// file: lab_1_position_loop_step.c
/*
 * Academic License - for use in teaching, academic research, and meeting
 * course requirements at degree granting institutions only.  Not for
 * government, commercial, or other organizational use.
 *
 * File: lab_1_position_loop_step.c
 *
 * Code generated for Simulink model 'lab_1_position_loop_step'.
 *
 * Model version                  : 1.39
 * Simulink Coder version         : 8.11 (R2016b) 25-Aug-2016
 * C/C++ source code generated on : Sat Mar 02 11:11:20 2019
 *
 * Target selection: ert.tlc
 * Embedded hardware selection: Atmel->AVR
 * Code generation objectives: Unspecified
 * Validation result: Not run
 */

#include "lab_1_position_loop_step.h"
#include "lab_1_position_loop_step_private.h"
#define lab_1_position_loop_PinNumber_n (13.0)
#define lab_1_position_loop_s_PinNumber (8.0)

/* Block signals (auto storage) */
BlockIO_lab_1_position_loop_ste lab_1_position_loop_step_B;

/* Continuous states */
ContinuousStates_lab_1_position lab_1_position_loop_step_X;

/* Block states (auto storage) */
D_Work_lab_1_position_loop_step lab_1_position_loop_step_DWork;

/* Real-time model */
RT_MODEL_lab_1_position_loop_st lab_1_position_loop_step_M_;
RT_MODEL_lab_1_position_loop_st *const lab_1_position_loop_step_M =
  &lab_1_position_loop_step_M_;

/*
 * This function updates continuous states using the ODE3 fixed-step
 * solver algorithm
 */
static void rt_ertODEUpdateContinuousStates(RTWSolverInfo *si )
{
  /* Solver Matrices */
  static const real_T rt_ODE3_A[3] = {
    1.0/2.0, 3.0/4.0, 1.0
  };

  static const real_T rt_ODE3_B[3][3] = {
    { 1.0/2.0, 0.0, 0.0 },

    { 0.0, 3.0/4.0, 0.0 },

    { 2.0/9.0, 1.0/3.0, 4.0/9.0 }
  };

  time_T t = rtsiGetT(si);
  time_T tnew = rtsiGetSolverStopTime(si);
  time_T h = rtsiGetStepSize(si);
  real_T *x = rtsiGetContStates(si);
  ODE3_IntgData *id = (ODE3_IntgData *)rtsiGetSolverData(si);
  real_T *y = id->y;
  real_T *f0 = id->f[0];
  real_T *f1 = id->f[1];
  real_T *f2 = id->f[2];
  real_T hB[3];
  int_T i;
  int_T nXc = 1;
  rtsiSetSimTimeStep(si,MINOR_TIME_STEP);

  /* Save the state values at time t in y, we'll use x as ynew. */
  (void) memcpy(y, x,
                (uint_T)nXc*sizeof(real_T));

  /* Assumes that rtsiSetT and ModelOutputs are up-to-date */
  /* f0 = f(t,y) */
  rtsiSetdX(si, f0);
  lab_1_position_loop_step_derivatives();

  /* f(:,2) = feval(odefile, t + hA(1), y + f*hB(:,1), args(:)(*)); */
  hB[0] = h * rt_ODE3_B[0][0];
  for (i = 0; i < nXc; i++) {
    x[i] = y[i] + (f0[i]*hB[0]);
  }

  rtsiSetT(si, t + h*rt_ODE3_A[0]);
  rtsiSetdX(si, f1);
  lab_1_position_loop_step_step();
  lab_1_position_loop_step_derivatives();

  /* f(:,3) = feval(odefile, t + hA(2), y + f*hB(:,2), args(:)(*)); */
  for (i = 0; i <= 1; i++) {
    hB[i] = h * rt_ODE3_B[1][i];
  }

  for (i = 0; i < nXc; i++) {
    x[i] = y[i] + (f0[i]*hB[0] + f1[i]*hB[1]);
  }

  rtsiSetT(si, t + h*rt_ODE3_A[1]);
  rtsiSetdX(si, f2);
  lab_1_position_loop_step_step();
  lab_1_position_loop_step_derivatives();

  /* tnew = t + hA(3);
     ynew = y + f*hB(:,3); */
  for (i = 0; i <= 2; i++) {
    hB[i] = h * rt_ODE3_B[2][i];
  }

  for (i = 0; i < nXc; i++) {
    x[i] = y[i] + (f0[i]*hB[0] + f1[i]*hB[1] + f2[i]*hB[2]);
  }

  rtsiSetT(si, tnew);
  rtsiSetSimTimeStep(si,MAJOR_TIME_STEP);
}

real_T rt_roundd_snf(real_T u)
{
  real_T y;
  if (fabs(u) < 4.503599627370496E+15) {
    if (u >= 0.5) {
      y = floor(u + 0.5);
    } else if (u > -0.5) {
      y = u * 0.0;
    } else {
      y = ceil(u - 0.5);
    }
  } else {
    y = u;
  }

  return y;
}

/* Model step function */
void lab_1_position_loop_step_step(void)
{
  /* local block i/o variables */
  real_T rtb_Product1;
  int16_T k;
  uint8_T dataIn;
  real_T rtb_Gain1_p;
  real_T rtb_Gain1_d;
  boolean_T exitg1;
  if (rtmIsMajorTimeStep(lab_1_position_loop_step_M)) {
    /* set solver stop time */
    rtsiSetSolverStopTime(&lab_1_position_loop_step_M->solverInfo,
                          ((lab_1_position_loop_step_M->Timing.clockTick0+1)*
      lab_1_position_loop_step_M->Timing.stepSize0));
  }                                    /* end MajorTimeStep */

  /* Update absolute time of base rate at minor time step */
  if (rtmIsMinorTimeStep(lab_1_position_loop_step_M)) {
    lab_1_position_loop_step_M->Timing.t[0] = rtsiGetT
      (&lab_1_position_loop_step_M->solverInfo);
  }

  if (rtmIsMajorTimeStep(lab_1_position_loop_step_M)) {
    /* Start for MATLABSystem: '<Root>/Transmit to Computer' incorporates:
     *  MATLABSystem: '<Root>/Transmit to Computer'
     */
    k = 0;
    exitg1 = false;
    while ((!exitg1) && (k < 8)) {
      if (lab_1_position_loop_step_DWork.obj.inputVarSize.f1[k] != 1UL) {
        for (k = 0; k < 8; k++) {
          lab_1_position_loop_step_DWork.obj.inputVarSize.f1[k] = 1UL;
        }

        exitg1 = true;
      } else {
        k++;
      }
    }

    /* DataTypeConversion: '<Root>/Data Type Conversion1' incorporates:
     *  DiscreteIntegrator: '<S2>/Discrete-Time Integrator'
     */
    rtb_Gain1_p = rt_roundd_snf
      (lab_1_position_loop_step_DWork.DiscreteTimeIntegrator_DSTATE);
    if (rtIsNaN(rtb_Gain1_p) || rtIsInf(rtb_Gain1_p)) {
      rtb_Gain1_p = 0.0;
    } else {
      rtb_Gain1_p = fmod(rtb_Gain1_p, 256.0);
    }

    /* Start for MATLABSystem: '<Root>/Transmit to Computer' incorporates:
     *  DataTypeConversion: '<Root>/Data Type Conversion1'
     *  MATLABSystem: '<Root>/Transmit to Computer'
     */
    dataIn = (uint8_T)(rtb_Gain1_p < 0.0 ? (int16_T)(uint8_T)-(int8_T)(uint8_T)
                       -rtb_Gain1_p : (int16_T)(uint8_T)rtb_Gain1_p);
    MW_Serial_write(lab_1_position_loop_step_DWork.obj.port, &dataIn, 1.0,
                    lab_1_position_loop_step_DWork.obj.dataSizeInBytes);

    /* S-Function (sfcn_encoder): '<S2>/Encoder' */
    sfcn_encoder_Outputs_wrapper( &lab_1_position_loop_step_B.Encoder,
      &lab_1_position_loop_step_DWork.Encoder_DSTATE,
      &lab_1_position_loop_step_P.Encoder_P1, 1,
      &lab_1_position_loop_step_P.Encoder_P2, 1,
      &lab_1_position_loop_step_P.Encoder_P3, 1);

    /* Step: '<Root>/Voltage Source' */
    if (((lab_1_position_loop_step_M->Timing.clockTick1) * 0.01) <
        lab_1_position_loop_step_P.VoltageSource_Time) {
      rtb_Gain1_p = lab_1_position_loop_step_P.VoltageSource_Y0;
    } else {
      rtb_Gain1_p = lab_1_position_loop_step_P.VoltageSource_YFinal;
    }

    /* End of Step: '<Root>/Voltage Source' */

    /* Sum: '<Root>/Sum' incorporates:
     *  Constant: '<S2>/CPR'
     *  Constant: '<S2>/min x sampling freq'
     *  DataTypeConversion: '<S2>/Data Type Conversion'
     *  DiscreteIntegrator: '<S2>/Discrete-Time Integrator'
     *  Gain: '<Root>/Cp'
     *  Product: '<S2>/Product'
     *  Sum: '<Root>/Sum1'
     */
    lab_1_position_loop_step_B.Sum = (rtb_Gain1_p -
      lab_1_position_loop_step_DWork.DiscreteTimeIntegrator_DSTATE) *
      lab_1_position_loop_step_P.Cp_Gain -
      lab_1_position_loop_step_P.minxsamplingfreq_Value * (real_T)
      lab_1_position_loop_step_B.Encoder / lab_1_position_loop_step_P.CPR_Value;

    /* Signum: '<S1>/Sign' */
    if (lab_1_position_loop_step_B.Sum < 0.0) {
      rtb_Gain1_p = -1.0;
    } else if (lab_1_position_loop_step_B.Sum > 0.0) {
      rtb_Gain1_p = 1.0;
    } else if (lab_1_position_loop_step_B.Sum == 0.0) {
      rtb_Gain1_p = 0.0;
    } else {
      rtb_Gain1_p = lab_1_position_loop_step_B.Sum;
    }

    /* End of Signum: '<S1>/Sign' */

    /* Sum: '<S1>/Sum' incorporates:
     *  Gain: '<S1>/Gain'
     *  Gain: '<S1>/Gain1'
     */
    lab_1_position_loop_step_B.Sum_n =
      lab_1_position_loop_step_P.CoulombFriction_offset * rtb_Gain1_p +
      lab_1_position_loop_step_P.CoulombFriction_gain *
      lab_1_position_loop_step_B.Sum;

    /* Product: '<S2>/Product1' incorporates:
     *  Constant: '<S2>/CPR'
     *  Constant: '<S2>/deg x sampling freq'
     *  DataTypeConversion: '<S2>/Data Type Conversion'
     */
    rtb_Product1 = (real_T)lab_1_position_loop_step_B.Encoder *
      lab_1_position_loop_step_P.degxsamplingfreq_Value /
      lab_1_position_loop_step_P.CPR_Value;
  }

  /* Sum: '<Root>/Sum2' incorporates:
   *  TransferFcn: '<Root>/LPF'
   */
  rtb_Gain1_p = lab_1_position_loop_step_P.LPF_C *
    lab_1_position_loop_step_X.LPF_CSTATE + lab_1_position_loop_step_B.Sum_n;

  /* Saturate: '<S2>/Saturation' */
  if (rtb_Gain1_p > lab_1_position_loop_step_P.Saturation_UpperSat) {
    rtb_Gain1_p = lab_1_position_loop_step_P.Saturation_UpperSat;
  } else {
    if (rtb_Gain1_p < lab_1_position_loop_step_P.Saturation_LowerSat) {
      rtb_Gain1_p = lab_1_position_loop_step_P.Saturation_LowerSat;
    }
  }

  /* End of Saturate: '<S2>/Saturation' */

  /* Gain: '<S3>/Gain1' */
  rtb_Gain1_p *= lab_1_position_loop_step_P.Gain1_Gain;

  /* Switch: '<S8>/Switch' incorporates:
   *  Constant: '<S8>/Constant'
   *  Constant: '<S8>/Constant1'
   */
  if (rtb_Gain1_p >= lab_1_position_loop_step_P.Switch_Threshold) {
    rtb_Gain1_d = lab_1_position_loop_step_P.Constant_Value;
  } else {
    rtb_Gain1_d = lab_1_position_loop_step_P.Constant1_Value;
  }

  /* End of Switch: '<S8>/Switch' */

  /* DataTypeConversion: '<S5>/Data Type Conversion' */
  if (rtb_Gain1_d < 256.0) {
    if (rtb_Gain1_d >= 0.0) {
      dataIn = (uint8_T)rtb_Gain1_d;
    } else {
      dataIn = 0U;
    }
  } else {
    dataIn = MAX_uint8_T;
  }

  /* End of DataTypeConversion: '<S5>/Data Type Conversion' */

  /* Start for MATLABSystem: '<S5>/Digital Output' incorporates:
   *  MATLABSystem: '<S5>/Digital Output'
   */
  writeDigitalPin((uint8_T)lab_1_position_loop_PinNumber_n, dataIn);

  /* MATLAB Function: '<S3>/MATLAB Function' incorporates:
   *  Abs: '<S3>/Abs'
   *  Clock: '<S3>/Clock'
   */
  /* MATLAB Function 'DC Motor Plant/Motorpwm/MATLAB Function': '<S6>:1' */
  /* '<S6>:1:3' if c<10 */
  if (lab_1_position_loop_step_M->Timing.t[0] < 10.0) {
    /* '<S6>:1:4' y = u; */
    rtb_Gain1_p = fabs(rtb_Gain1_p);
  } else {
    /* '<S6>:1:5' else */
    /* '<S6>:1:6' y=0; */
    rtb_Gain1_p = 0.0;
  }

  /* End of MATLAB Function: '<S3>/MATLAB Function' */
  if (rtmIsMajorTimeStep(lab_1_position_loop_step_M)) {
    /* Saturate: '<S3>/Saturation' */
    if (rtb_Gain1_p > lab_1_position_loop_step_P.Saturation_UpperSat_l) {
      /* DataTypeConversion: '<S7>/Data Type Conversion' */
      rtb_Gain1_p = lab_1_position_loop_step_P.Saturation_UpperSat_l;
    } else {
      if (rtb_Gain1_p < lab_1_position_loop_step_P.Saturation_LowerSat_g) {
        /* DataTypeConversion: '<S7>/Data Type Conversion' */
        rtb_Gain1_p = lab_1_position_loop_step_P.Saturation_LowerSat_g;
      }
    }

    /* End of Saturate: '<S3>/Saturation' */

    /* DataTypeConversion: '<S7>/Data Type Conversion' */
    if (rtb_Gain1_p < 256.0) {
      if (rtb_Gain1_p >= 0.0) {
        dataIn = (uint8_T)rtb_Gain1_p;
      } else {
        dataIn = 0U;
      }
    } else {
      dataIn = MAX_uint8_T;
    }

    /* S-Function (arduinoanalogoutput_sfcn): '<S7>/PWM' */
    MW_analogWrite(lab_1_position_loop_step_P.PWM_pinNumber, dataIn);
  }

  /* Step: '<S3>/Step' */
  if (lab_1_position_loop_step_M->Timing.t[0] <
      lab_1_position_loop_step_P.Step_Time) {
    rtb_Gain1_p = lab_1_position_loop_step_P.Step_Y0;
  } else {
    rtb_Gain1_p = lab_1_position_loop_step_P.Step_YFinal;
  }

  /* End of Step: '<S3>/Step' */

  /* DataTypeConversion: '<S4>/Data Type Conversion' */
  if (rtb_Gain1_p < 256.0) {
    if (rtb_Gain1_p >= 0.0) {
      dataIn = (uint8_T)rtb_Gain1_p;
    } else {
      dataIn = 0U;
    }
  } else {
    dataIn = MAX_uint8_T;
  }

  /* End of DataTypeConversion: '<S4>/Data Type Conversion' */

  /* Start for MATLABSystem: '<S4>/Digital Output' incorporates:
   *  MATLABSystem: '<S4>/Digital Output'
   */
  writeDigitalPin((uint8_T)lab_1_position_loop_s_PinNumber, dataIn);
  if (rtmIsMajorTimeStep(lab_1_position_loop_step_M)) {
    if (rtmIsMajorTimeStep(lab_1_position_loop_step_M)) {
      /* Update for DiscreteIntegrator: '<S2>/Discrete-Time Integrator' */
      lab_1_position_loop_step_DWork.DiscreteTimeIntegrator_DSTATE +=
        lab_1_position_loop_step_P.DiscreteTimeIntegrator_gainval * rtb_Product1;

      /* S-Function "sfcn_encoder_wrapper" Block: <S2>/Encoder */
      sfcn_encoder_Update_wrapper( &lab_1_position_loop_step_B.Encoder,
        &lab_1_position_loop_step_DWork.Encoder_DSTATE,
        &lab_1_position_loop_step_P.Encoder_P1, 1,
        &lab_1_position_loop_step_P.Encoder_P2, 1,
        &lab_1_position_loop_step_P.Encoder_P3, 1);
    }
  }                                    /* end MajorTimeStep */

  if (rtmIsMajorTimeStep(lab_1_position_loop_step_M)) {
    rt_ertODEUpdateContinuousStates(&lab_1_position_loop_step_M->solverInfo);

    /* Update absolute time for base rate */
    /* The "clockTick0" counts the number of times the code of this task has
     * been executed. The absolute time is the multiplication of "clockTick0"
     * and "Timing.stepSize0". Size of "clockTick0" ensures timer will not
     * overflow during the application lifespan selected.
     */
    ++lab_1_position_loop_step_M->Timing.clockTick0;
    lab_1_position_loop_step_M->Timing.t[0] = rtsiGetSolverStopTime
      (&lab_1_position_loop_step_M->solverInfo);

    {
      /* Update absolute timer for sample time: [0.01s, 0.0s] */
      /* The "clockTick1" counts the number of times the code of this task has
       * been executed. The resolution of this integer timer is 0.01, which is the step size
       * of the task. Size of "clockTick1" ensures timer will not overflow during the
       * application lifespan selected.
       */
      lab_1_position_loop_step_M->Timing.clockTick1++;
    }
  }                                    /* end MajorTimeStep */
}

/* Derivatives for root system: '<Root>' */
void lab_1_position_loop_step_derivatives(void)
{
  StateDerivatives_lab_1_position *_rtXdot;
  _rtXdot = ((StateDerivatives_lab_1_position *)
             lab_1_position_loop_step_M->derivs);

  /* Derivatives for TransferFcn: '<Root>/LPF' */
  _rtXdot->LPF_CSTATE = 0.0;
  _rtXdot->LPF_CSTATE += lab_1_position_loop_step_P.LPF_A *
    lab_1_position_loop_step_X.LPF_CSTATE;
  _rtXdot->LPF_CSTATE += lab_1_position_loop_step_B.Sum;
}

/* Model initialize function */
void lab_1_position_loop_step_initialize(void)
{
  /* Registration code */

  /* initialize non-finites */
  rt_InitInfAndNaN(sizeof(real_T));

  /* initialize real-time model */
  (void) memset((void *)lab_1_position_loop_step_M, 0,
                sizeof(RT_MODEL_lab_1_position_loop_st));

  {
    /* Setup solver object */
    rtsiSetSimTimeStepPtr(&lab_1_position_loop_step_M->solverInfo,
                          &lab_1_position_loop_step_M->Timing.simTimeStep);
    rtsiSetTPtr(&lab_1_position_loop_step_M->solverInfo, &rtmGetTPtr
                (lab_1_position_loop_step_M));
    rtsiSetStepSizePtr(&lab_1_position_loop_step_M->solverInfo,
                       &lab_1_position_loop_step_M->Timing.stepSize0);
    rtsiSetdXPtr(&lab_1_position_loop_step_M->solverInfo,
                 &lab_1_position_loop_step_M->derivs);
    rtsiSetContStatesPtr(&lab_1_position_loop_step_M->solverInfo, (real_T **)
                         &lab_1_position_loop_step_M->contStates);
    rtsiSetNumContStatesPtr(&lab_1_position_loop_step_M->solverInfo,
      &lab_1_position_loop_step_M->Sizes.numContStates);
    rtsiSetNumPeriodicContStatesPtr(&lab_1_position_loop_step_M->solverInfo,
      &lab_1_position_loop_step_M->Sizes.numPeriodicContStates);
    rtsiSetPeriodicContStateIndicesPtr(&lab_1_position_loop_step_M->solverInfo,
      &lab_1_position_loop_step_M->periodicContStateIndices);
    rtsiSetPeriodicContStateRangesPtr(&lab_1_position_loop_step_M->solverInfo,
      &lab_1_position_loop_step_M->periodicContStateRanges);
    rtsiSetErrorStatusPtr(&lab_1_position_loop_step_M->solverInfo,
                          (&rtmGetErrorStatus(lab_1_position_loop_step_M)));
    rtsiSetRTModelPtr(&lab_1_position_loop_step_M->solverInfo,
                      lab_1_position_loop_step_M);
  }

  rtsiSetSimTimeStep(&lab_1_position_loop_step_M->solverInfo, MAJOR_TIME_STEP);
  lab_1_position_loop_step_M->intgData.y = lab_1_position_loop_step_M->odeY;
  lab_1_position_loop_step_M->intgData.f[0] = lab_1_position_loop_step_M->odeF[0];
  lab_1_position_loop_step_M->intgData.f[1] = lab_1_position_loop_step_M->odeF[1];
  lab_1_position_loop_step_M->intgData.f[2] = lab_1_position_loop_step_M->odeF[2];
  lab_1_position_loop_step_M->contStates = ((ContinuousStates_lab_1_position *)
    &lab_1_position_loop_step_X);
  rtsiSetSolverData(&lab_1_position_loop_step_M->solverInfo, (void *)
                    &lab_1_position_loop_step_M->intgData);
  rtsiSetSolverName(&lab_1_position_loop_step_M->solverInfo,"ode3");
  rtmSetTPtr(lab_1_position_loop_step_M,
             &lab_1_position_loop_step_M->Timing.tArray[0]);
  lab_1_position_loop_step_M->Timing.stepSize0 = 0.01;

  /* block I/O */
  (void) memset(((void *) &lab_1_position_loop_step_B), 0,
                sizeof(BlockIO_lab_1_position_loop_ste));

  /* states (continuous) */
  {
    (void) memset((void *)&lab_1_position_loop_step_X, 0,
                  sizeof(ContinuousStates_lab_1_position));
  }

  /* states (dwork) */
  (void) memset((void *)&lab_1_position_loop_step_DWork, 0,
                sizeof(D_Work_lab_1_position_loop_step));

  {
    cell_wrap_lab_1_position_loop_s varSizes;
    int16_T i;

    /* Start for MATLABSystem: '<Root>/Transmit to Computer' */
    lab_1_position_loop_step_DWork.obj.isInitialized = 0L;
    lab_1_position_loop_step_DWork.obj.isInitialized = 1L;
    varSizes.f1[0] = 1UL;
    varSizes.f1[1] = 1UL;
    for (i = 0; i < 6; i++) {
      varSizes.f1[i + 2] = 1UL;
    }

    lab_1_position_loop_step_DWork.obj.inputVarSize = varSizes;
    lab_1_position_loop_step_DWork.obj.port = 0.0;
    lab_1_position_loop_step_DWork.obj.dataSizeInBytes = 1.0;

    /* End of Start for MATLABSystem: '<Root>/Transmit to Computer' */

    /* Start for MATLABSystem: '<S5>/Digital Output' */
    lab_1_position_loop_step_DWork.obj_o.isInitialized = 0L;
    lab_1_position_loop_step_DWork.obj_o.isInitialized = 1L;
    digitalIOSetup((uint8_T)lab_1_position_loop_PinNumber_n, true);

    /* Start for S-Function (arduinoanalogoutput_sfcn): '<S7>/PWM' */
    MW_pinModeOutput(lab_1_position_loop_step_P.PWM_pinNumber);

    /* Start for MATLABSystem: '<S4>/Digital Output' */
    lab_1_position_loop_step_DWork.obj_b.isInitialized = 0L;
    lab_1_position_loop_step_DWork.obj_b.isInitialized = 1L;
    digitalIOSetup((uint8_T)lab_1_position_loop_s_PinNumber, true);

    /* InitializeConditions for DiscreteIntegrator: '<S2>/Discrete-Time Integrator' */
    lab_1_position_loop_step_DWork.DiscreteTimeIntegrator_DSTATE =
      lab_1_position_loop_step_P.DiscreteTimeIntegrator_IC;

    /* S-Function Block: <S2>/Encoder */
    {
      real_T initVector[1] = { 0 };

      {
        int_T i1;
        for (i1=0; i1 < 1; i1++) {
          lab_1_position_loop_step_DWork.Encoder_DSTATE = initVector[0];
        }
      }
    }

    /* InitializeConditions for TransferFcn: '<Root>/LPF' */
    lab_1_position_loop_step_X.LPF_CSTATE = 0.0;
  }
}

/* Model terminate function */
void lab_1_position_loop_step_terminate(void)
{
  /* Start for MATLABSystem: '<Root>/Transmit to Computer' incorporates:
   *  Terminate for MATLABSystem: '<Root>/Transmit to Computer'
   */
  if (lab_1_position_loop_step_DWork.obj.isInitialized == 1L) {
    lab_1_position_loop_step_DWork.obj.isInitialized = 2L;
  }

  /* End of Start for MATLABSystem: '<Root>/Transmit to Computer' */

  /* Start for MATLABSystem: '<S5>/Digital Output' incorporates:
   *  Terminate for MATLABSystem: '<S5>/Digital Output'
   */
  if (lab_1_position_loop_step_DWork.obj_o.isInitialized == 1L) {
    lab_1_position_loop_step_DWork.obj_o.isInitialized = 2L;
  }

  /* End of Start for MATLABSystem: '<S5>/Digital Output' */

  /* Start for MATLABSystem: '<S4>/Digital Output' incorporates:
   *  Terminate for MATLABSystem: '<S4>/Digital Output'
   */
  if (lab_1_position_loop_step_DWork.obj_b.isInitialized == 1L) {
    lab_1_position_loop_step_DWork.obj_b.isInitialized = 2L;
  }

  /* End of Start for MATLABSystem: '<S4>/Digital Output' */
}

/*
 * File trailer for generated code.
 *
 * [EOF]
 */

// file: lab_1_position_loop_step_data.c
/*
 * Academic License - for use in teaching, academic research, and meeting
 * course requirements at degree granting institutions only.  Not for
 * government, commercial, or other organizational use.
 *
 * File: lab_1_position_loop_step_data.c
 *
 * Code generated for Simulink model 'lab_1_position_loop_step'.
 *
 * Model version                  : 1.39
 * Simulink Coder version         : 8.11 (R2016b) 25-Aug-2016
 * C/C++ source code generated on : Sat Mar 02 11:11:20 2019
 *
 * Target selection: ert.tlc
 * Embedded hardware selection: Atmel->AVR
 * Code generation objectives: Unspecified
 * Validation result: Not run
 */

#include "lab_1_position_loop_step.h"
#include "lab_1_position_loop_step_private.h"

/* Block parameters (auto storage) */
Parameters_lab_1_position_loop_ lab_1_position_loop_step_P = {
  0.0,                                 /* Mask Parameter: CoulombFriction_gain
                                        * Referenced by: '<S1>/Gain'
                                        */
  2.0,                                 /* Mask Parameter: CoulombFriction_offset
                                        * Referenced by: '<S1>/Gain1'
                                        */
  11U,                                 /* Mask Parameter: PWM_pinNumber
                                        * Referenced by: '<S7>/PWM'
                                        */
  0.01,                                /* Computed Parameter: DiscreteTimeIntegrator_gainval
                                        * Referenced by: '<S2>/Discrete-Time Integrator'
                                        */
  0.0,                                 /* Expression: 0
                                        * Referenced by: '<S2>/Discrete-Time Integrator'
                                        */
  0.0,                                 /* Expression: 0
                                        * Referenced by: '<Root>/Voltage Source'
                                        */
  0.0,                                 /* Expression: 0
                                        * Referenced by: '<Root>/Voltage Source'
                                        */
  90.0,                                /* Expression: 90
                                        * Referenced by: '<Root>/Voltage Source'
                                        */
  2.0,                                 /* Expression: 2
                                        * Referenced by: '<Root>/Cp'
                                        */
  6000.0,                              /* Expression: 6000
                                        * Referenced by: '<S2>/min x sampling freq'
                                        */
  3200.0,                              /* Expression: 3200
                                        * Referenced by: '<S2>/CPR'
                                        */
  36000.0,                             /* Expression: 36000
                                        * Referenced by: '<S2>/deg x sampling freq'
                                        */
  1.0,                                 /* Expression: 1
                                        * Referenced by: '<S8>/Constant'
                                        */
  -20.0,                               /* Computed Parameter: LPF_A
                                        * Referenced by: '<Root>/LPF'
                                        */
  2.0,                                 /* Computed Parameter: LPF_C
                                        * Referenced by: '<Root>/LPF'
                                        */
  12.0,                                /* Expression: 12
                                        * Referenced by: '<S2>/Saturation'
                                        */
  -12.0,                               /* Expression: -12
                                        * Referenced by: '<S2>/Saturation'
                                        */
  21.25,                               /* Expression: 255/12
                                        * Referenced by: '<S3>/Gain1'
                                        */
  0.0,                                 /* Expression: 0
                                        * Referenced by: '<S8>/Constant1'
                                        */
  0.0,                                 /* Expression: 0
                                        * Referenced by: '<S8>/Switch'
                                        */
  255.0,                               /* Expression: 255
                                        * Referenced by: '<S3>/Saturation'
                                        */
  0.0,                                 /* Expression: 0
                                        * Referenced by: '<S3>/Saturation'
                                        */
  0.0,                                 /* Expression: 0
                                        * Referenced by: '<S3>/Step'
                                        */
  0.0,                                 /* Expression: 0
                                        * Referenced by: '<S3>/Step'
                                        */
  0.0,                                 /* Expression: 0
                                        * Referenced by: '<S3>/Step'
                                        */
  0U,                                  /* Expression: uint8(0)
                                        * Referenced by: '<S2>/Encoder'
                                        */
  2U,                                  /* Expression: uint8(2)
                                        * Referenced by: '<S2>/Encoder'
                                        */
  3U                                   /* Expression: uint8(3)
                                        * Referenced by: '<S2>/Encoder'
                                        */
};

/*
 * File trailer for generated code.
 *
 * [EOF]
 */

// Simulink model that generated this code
simulink model "lab_1_position_loop_step"  (R2016b)
settings: Solver=ode3  StartTime=0.0  StopTime=10  FixedStep=0.01  RelTol=1e-3
undefined symbols (not defined in the file or in its folder): DiscIntNeverNeededParam
libraries: arduinolib x4, simulink x1, neural x1

== system lab_1_position_loop_step ==
  Coulomb Friction : simulink/Discontinuities/Coulomb & Viscous Friction  offset=2  gain=0
  Cp : Gain  Gain=9
  DC Motor Plant : Subsystem
  Data Type Conversion1 : DataTypeConversion  OutDataTypeStr=uint8  RndMeth=Round
  LPF : TransferFcn  Numerator=[0.01]  Denominator=[0.08 1]
  Sum : Sum  Inputs=|+-
  Sum1 : Sum  Inputs=|+-
  Sum2 : Sum  Inputs=|++
  Transmit to Computer : arduinolib/Serial Transmit  portNumber=0  blockPlatform=arduino
  Voltage Source : Step  Time=0  After=90  SampleTime=0.01
  wires:
  DC Motor Plant/1(Position (deg)) -> Sum1/2, Data Type Conversion1/1
  Data Type Conversion1/1 -> Transmit to Computer/1
  Sum/1 -> LPF/1, Coulomb Friction/1
  Cp/1 -> Sum/1
  Sum2/1 -> DC Motor Plant/1(Voltage (V))
  DC Motor Plant/2(Velocity (rpm)) -> Sum/2
  Sum1/1 -> Cp/1
  Voltage Source/1 -> Sum1/1
  LPF/1 -> Sum2/1
  Coulomb Friction/1 -> Sum2/2

== system lab_1_position_loop_step/DC Motor Plant ==
  Voltage (V) : Inport
  CPR : Constant  Value=3200
  Data Type Conversion : DataTypeConversion  OutDataTypeStr=double  RndMeth=Round
  Discrete-Time Integrator : DiscreteIntegrator  InitialConditionSetting=State (most efficient)  SampleTime=-1  ICPrevOutput=DiscIntNeverNeededParam  ICPrevScaledInput=DiscIntNeverNeededParam
  Encoder : S-Function  InitFcn=try, set_param(gcb,'FunctionName','sfcn_encoder'), end  FunctionName=sfcn_encoder  Parameters=uint8(0),uint8(2),uint8(3)  SFunctionModules=sfcn_encoder_wrapper  SFunctionDeploymentMode=off  EnableBusSupport=off  mask(S-Function Builder){}
      mask init:
      | val = [[.9  0.75 0.75 1 1 .9 .9 1]',[1 1 0.75 0.75 .9 .9 1 .9]'];try , sys = get_param(gcb,'SfunBuilderFcnName');if isempty(sys), sys = get_param(gcb,'FunctionName'); end,catch, sys = get_param(gcb,'FunctionName'); end
  Motorpwm : Subsystem
  Product : Product  Inputs=**/
  Product1 : Product  Inputs=**/
  Saturation : Saturate  UpperLimit=12  LowerLimit=-12
  deg x sampling freq : Constant  Value=36000
  min x sampling freq : Constant  Value=6000
  Position (deg) : Outport
  Velocity (rpm) : Outport  Port=2
  wires:
  Encoder/1 -> Data Type Conversion/1
  Voltage (V)/1 -> Saturation/1
  Data Type Conversion/1 -> Product1/1, Product/2
  Product/1 -> Velocity (rpm)/1
  min x sampling freq/1 -> Product/1
  Product1/1 -> Discrete-Time Integrator/1
  deg x sampling freq/1 -> Product1/2
  Discrete-Time Integrator/1 -> Position (deg)/1
  CPR/1 -> Product1/3, Product/3
  Saturation/1 -> Motorpwm/1(In1)

== system lab_1_position_loop_step/DC Motor Plant/Motorpwm ==
  In1 : Inport
  Abs : Abs
  Brake : arduinolib/Digital Output  pinNumber=8  blockPlatform=arduino
  Clock : Clock
  "Direction " : arduinolib/Digital Output  pinNumber=13  blockPlatform=arduino
  Gain1 : Gain  Gain=255/12
  MATLAB Function : MATLAB Function  TreatAsAtomicUnit=on
  PWM : arduinolib/PWM  pinNumber=11  blockPlatform=arduino
  Saturation : Saturate  UpperLimit=255  LowerLimit=0
  Step : Step  Time=0  After=0  SampleTime=0
  hardlim : neural/Transfer Functions/hardlim
  wires:
  hardlim/1 -> "Direction "/1
  Step/1 -> Brake/1
  Saturation/1 -> PWM/1
  In1/1 -> Gain1/1
  MATLAB Function/1(y) -> Saturation/1
  Abs/1 -> MATLAB Function/1(u)
  Clock/1 -> MATLAB Function/2(c)
  Gain1/1 -> hardlim/1, Abs/1

== matlab function lab_1_position_loop_step/DC Motor Plant/Motorpwm/MATLAB Function ==
function y = fcn(u,c)
%#codegen
if c<10
    y = u;
else
    y=0;
end
